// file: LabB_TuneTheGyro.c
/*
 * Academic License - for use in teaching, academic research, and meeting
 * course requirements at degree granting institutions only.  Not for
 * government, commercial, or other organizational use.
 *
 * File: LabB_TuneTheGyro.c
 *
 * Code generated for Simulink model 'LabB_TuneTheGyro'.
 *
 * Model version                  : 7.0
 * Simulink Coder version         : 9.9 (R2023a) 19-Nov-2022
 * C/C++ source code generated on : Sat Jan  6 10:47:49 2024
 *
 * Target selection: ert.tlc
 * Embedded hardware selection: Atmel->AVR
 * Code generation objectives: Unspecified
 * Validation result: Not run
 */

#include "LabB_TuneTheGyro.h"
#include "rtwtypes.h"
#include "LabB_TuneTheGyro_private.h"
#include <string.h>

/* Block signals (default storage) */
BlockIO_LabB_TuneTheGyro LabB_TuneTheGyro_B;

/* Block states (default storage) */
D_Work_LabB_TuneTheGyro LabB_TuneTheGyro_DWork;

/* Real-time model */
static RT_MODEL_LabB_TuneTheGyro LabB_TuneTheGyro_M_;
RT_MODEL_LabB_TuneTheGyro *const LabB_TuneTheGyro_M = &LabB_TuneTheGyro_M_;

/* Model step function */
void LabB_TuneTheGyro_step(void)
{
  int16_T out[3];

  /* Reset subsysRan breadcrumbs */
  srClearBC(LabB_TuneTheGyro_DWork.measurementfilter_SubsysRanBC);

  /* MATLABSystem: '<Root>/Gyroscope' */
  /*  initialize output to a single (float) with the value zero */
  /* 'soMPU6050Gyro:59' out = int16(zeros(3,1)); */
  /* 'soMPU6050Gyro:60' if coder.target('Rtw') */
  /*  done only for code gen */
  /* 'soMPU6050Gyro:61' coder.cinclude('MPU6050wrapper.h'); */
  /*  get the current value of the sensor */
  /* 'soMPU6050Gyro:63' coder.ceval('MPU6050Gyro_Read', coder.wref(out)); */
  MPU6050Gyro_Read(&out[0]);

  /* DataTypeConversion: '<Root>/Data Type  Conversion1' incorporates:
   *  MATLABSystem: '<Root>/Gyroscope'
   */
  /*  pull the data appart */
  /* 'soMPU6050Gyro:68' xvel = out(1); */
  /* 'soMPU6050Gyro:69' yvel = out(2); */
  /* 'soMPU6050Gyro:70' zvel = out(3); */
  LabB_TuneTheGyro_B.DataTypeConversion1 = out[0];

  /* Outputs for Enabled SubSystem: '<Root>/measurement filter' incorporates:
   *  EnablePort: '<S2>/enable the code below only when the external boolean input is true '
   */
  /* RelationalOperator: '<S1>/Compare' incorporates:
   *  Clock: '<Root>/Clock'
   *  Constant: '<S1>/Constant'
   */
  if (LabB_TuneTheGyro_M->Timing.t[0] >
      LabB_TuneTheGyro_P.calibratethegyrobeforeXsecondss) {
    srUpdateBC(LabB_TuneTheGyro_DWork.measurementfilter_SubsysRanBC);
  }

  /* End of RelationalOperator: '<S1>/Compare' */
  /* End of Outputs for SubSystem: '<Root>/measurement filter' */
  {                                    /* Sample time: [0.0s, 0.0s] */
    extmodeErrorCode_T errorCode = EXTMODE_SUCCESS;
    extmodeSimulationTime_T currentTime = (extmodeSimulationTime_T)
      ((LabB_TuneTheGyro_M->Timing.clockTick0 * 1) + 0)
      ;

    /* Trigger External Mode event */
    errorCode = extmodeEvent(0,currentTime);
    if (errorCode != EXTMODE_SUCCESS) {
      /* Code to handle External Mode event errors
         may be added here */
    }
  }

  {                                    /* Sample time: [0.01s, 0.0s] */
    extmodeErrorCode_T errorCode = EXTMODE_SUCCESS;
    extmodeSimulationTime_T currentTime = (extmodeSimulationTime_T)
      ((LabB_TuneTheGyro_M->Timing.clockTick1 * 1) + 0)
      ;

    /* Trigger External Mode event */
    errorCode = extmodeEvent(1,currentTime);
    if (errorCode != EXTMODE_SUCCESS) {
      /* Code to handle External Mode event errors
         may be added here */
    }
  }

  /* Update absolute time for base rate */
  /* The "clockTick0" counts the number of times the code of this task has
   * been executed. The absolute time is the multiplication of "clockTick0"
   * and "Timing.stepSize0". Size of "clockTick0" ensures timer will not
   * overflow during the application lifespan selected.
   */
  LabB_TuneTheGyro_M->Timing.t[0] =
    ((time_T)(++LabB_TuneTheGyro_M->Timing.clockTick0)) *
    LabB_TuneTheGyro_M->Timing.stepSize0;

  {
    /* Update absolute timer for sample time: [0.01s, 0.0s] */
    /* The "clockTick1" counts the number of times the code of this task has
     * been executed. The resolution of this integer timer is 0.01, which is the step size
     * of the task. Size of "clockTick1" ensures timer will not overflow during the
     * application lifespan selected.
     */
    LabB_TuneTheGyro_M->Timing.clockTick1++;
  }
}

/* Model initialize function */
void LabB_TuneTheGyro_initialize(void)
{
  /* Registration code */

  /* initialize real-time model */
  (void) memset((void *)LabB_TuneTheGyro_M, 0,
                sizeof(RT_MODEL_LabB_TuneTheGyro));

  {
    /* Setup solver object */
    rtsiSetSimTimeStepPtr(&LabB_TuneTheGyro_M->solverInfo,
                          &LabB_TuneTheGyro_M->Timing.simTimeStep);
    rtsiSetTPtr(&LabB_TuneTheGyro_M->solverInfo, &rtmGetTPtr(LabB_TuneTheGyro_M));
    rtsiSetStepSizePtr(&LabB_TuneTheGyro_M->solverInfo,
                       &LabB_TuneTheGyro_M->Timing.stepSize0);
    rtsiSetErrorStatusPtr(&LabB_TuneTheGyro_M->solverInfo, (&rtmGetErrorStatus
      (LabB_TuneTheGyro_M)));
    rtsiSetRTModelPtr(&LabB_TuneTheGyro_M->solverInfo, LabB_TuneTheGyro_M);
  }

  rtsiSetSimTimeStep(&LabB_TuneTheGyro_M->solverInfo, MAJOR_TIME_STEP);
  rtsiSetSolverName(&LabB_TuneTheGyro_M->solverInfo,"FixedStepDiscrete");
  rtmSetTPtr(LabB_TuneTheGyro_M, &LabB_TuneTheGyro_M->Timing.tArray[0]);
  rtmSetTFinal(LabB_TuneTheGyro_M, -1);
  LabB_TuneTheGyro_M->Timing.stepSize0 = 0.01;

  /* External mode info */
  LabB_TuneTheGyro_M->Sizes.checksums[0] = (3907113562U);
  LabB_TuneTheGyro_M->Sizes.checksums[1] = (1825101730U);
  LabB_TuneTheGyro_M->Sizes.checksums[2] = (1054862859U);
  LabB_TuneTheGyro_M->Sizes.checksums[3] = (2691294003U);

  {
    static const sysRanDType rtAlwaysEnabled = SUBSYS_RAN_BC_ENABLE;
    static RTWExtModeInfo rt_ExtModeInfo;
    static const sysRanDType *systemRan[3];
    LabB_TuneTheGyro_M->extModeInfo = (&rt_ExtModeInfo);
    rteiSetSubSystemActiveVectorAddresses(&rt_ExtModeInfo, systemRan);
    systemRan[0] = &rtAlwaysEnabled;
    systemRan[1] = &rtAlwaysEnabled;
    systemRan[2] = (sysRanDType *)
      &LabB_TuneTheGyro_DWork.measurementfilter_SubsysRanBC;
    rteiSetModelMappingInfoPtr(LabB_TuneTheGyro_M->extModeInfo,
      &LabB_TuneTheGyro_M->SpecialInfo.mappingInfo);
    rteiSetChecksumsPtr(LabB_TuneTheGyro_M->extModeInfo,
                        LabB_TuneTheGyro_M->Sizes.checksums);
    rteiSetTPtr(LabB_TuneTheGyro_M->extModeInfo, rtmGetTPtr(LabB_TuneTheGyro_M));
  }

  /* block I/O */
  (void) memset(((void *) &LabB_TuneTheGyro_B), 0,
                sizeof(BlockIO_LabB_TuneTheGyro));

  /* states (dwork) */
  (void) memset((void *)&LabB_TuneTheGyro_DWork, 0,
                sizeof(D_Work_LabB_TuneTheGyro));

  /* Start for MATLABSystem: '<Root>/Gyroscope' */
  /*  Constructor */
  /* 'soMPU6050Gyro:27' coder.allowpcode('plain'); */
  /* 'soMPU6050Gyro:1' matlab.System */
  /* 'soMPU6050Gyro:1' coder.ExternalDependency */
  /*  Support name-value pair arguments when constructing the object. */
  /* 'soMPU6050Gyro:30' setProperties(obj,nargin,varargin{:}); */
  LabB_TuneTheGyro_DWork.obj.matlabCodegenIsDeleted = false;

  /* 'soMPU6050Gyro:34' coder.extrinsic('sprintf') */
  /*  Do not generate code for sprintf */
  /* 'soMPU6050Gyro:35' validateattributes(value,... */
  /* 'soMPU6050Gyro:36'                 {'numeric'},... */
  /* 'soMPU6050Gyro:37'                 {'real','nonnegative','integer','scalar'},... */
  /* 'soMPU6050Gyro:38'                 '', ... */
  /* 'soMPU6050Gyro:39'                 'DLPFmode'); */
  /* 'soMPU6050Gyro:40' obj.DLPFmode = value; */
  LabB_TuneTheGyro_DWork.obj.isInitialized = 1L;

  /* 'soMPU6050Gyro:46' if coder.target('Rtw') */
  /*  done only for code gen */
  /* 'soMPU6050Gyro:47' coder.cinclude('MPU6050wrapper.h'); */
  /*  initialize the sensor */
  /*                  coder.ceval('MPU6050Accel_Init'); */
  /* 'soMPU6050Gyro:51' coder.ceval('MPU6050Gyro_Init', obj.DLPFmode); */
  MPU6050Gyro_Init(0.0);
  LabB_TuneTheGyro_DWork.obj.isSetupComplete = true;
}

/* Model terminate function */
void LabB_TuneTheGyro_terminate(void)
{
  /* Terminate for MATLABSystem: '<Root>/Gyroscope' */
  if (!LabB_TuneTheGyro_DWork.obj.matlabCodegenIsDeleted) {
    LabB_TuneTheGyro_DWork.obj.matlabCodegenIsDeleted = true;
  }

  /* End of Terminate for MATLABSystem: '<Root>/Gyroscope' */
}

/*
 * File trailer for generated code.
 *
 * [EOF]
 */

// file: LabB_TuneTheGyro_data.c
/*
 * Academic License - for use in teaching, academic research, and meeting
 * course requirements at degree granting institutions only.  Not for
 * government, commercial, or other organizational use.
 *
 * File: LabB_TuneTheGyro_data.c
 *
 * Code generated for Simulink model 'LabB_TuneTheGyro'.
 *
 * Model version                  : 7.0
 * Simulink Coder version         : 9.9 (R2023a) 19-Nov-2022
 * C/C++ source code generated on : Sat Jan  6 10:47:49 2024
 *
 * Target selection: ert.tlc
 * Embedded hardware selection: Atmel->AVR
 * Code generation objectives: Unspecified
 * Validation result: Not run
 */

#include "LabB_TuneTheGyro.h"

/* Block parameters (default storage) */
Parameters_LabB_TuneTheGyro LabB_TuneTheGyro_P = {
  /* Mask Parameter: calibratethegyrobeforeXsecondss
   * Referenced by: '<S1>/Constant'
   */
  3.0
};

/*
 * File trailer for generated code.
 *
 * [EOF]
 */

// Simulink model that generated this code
simulink model "LabB_TuneTheGyro"  (R2023a)
settings: Solver=FixedStepDiscrete  StartTime=0.0  StopTime=inf  FixedStep=fSamplingPeriod  RelTol=1e-3  EnableMultiTasking=on
libraries: simulink x1

== system LabB_TuneTheGyro ==
  Clock : Clock
  Data Type Conversion1 : DataTypeConversion  OutDataTypeStr=double  SaturateOnIntegerOverflow=off  RndMeth=Floor
  Gyroscope : MATLABSystem  System=soMPU6050Gyro  DLPFmode=0
  Scope : Scope
  Terminator : Terminator
  Terminator1 : Terminator
  "calibrate the gyro before X seconds, start controlling after X seconds" : simulink/Logic and Bit Operations/Compare To Constant  relop=>  const=3  OutDataTypeStr=boolean
  measurement filter : Subsystem
  wires:
  Clock/1 -> "calibrate the gyro before X seconds, start controlling after X seconds"/1
  "calibrate the gyro before X seconds, start controlling after X seconds"/1 -> measurement filter/Enable
  Data Type Conversion1/1 -> Scope/1, measurement filter/1(gyro bias)
  Gyroscope/1 -> Data Type Conversion1/1
  Gyroscope/2 -> Terminator/1
  Gyroscope/3 -> Terminator1/1

== system LabB_TuneTheGyro/measurement filter ==
  gyro bias : Inport
  "enable the code below only when the external boolean input is true " : EnablePort
  Scope : Scope
  wires:
  gyro bias/1 -> Scope/1
